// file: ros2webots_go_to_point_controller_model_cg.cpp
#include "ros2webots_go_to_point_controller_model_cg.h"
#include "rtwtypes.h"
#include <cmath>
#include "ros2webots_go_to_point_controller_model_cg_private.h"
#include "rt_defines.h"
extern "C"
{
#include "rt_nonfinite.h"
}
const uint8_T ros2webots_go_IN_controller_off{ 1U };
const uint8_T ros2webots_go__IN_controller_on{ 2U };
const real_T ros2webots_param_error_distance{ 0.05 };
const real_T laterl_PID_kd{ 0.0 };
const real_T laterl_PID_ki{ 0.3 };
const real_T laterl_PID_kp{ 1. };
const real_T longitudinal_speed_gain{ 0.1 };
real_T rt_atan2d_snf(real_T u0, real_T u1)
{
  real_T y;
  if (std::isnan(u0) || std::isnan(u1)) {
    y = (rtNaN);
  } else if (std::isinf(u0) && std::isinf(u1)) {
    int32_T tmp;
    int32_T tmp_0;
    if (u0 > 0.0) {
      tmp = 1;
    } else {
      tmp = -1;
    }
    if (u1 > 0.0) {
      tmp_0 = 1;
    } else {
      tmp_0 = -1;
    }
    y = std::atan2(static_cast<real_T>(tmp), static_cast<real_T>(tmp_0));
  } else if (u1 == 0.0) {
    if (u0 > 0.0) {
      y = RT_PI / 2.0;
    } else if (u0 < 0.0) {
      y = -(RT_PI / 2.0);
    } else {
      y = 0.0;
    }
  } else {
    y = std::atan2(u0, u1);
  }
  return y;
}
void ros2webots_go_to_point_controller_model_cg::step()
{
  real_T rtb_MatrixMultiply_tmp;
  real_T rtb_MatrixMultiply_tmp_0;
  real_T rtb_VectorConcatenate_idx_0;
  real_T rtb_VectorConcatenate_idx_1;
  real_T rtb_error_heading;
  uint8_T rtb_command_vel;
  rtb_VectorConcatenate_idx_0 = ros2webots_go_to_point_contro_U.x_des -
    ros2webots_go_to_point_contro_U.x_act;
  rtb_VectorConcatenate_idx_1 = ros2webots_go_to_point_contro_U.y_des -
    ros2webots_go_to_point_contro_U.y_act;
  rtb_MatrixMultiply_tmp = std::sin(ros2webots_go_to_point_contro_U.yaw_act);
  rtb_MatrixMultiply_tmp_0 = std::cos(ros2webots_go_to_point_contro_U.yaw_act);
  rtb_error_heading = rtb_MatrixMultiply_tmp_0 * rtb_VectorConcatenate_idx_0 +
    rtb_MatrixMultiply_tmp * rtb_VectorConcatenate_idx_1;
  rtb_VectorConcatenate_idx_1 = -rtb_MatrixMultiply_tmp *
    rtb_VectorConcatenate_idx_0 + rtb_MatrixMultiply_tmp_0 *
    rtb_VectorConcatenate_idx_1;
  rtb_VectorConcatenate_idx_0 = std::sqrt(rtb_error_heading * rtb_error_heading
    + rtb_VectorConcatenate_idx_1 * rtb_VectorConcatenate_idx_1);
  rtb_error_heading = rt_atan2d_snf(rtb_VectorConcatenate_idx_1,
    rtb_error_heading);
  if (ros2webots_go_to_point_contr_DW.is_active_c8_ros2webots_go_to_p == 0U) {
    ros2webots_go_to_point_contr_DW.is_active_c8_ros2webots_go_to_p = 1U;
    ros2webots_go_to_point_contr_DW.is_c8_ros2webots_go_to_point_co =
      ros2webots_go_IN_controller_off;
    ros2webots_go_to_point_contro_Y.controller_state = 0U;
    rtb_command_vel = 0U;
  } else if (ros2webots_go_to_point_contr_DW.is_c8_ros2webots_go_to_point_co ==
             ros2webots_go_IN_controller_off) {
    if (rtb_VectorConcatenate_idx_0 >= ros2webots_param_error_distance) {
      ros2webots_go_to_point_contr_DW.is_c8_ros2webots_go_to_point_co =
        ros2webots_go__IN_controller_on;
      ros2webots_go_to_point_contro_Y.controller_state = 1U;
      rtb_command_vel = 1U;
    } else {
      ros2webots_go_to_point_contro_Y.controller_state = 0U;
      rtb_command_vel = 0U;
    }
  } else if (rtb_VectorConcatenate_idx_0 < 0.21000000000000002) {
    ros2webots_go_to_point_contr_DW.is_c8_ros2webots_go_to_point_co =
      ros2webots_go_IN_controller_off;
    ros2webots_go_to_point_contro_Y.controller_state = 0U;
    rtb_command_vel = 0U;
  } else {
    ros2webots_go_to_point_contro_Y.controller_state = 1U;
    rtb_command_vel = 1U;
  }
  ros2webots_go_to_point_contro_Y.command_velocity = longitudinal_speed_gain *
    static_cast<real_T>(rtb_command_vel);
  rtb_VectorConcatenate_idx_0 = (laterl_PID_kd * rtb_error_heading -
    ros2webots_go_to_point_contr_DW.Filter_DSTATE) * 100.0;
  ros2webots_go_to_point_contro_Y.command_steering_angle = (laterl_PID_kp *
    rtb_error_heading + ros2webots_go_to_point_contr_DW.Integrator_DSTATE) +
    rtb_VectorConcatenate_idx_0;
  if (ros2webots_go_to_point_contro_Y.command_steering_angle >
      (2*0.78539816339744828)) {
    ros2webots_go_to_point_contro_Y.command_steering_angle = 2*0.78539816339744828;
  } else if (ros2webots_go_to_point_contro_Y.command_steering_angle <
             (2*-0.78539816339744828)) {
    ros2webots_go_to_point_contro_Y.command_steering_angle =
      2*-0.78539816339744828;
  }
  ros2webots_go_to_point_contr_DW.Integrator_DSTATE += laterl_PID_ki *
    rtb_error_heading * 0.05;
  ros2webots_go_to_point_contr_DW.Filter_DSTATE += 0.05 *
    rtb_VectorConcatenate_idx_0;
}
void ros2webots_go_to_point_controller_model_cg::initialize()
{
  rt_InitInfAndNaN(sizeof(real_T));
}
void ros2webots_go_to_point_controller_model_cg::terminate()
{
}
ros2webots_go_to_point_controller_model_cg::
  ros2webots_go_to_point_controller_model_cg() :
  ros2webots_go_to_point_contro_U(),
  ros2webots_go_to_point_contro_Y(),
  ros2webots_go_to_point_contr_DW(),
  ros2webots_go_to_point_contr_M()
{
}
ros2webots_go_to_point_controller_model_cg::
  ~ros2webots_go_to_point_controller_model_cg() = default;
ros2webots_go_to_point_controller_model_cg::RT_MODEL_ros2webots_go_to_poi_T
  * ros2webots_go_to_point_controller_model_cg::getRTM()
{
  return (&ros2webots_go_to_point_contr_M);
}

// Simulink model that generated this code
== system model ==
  x_des : Inport
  y_des : Inport
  Inport#1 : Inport
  x_act : Inport
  y_act : Inport
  yaw_act : Inport
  controller_state : Outport  <- 1: Stateflowchart#1
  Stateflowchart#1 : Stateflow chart  <- 1: MATLABFunction#1
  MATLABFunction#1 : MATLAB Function  <- 1: MatrixMultiply
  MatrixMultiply : Product  Multiplication=Matrix(*)  <- 1: MATLABFunction#2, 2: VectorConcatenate
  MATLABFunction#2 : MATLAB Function  <- 1: yaw_act
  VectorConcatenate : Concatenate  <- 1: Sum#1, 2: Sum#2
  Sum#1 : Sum  Inputs=+-  <- 1: x_des, 2: x_act
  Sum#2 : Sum  Inputs=+-  <- 1: y_des, 2: y_act
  command_velocity : Outport  <- 1: Gain#1
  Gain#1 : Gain  Gain=longitudinal_speed_gain  <- 1: DataTypeConversion#1
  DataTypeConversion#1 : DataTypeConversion  <- 1: Stateflowchart#1/2
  command_steering_angle : Outport  <- 1: Saturate#1
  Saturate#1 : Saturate  UpperLimit=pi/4  LowerLimit=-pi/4  <- 1: PIDController#1
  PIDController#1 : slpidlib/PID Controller  Controller=PID  Form=Parallel  TimeDomain=Discrete-time  IntegratorMethod=Forward Euler  P=laterl_PID_kp  I=laterl_PID_ki  D=laterl_PID_kd  N=100  InitialConditionForIntegrator=0  ExternalReset=none  LimitOutput=off  UpperSaturationLimit=inf  LowerSaturationLimit=-inf  <- 1: MATLABFunction#1/2
== stateflow chart Stateflowchart#1 ==
  state controller_off
    controller_state = 0;
    command_vel = 0;
  state controller_on
    controller_state = 1;
    command_vel = 1;
  (default) -> controller_off
  controller_off -> controller_on : [error_distance >=... param_error_distance]
  controller_on -> controller_off : [error_distance <... 1.05*param_error_distance]
  data: controller_state output uint8; error_distance input; param_error_distance constant double =0.20; command_vel output uint8

== matlab function MATLABFunction#1 ==
function [error_dist, error_heading] = tracking_error(vec_r_rel_xy)

error_dist = sqrt(vec_r_rel_xy(1)^2 + vec_r_rel_xy(2)^2);
error_heading = atan2(vec_r_rel_xy(2), vec_r_rel_xy(1)); % <0 --> turns left, >0 --> turns right

== matlab function MATLABFunction#2 ==
function rotation_matrix = rotate_2d_around_Z(yaw_angle)

r_11 = cos(yaw_angle);
r_12 = sin(yaw_angle);
r_21 = -sin(yaw_angle);
r_22 = cos(yaw_angle);

rotation_matrix = [r_11, r_12; r_21, r_22];

== stateflow chart Stateflowchart#1 ==
  state p0
    x=5;
    y = 0;
  state p1
    x=5;
    y = 3;
  state p2
    x=-5;
    y = 3;
  state p3
    x=-5;
    y = 0;
  state p4
    x=0;
    y = 0;
  (default) -> p0
  p0 -> p1 : [point_reached==0]
  p1 -> p2 : [point_reached==0]
  p2 -> p3 : [point_reached==0]
  p3 -> p4 : [point_reached==0]
  data: x output; y output; point_reached input

== stateflow chart Stateflowchart#1 ==
  state controller_off
    controller_state = 0;
    command_vel = 0;
  state controller_on
    controller_state = 1;
    command_vel = 1;
  (default) -> controller_off
  controller_off -> controller_on : [error_distance >=... param_error_distance]
  controller_on -> controller_off : [error_distance <... 1.05*param_error_distance]
  data: controller_state output uint8; error_distance input; param_error_distance constant double =0.20; command_vel output uint8

== matlab function MATLABFunction#1 ==
function [error_dist, error_heading] = tracking_error(vec_r_rel_xy)

error_dist = sqrt(vec_r_rel_xy(1)^2 + vec_r_rel_xy(2)^2);
error_heading = atan2(vec_r_rel_xy(2), vec_r_rel_xy(1)); % <0 --> turns left, >0 --> turns right

== matlab function MATLABFunction#2 ==
function rotation_matrix = rotate_2d_around_Z(yaw_angle)

r_11 = cos(yaw_angle);
r_12 = sin(yaw_angle);
r_21 = -sin(yaw_angle);
r_22 = cos(yaw_angle);

rotation_matrix = [r_11, r_12; r_21, r_22];
